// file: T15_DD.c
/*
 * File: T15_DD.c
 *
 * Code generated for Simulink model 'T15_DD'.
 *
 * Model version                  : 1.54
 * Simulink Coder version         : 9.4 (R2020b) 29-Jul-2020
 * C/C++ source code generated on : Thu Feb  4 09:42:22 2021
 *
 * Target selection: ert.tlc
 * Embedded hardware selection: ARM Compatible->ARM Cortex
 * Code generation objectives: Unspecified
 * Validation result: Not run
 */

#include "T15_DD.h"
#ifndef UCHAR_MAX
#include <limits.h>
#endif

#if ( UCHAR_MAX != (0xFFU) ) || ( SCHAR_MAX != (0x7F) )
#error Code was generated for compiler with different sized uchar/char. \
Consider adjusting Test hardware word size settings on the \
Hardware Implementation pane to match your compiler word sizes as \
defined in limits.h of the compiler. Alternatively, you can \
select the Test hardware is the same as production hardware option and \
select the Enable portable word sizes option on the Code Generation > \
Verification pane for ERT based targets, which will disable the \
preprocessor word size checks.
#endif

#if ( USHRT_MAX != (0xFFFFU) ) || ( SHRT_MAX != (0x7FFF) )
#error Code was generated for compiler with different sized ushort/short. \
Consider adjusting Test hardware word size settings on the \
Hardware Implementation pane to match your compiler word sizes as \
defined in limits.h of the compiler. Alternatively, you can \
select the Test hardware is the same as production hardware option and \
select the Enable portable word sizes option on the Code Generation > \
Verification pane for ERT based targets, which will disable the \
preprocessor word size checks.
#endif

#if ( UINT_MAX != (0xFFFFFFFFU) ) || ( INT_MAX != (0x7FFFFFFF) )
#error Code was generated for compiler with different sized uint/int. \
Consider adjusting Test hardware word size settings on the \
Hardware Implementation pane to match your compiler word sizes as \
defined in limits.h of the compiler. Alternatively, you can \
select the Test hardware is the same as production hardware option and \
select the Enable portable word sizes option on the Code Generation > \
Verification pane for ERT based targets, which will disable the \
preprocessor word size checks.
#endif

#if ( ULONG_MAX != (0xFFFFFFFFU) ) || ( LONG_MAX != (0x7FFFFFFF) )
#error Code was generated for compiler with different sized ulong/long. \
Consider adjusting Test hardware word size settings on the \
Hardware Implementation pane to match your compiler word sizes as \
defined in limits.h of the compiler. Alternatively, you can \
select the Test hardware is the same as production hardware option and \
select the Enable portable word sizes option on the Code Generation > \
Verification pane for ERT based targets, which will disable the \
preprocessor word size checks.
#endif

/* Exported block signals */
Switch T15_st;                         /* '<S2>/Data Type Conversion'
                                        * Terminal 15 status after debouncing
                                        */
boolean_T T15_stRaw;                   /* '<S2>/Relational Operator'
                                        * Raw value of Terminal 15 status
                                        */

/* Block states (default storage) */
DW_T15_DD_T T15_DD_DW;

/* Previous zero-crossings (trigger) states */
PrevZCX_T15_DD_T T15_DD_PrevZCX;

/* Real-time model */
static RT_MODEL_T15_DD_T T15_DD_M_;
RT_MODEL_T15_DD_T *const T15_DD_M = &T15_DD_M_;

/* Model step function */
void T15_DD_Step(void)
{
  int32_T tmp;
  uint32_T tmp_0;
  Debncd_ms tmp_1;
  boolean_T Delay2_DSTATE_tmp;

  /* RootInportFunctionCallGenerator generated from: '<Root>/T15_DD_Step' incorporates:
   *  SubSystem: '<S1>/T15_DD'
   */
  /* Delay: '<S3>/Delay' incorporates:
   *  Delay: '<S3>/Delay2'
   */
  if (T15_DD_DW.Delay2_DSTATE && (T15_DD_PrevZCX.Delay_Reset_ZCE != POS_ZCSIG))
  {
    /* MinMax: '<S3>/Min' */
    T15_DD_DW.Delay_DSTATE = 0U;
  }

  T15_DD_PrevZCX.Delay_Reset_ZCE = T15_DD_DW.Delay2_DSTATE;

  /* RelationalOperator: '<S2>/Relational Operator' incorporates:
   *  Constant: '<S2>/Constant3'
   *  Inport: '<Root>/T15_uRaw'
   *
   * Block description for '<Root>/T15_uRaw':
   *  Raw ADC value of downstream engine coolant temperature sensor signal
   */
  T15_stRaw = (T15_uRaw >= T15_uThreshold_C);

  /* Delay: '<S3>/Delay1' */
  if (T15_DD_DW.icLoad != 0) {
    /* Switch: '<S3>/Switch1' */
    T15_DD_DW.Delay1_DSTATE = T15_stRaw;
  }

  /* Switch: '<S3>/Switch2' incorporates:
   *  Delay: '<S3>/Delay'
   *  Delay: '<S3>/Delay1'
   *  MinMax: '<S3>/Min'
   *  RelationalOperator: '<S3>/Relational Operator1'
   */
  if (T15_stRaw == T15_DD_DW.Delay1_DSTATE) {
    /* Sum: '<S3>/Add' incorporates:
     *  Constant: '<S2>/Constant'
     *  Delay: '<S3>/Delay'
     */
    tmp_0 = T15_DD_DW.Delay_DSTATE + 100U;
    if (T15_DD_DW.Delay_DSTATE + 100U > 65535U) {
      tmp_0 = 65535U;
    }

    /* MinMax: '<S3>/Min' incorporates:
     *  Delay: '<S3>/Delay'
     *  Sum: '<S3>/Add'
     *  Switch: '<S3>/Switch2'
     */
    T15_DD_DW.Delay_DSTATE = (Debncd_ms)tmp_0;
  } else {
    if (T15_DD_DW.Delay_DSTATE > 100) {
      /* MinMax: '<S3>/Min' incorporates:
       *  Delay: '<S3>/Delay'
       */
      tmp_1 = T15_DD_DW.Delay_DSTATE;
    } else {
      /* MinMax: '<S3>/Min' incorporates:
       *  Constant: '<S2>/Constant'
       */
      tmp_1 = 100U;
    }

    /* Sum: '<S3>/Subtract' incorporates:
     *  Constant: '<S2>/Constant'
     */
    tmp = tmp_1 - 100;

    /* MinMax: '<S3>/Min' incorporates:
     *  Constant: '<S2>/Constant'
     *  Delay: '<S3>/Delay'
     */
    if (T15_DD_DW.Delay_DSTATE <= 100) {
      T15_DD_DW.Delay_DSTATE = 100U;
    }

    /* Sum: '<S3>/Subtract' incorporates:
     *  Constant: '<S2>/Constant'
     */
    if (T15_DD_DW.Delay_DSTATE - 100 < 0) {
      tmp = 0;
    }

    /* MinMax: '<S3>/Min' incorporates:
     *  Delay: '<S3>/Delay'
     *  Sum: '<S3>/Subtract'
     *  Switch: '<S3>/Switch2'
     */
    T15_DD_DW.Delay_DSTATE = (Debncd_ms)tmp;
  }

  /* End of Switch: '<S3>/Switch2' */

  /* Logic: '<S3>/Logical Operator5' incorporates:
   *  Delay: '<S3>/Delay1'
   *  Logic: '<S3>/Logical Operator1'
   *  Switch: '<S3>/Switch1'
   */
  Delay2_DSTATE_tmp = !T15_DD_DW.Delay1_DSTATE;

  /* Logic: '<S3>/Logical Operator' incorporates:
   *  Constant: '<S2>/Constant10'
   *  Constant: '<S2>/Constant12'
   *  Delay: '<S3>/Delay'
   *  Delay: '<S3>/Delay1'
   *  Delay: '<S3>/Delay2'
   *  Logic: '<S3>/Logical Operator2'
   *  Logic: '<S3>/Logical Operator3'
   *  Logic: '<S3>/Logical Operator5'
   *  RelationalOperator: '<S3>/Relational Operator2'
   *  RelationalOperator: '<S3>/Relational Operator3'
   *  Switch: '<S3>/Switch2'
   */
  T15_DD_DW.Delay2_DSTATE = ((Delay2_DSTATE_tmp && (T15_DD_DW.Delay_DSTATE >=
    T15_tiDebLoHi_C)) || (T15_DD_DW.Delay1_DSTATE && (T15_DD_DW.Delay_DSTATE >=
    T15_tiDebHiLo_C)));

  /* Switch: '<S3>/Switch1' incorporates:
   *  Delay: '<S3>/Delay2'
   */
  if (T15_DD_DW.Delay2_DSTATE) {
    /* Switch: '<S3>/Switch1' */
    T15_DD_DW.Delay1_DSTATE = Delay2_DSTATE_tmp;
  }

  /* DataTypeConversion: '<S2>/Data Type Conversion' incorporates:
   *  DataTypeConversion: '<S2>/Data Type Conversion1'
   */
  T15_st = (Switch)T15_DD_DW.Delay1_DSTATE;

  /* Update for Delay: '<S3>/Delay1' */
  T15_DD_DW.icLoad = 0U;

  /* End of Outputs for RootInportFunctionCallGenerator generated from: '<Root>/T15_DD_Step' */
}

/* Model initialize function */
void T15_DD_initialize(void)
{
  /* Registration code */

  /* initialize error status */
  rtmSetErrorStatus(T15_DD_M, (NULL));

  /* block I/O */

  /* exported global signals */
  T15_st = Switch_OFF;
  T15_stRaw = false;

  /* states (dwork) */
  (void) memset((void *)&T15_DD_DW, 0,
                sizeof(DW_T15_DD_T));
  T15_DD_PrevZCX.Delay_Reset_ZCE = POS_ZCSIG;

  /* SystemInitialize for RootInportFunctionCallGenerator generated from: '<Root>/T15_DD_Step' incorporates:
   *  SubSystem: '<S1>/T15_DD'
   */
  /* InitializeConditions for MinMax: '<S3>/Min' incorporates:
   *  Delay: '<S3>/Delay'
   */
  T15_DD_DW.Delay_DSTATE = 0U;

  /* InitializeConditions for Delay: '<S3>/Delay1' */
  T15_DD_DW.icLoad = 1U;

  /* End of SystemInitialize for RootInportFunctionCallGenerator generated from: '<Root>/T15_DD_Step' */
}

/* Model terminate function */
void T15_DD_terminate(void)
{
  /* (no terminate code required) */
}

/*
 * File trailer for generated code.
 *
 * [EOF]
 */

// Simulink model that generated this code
simulink model "T15_DD"  (R2018a)
settings: configuration reference "cs_ert" (kept outside this file)
model workspace (MAT data in the model file):
  T15_DD_DT = 10
values from neighbouring files (symbols this model uses):
  T15_tiDebHiLo_C = 10.0    [T15_DD.sldd]
  T15_tiDebLoHi_C = 10.0    [T15_DD.sldd]
  T15_uThreshold_C = 800.0    [T15_DD.sldd]
libraries: sllib x1

== system T15_DD ==
  T15_DD_Step : Inport  OutputFunctionCall=on
  T15_uRaw : Inport  Description=Raw ADC value of downstream engine coolant temperature sensor signal  Port=2  OutMin=0  OutMax=5000  OutDataTypeStr=Volt_mV  Unit=mv  PortDimensions=[1 1]
  Overview : Subsystem
  T15_st : Outport  Description=Terminal 15 status after debouncing  OutDataTypeStr=Enum:Switch  PortDimensions=[1 1]
  wires:
  T15_DD_Step/1 -> Overview/1(T15_DD_Step)
  T15_uRaw/1 -> Overview/2(T15_uRaw)
  Overview/1(T15_st) -> T15_st/1

== system T15_DD/Overview ==
  T15_DD_Step : Inport
  T15_uRaw : Inport  Port=2
  T15_DD : Subsystem
  T15_st : Outport
  wires:
  T15_uRaw/1 -> T15_DD/1(T15_uRaw)
  T15_DD/1(T15_st) -> T15_st/1
  T15_DD_Step/1 -> T15_DD/Trigger

== system T15_DD/Overview/T15_DD ==
  note: %大于800mv为高%
  T15_uRaw : Inport  Tag=mv
  Trigger : TriggerPort  TriggerType=function-call  VariantControl=Variant  PortDimensions=1
  Constant : Constant  Value=T15_DD_DT  OutDataTypeStr=Inherit: Inherit via back propagation
  Constant10 : Constant  Value=T15_tiDebLoHi_C
  Constant12 : Constant  Value=T15_tiDebHiLo_C
  Constant3 : Constant  Value=T15_uThreshold_C
  Data Type Conversion : DataTypeConversion
  Data Type Conversion1 : DataTypeConversion  OutDataTypeStr=uint8
  Debounce_DT : sllib/Debounce_DT
  Relational Operator : RelationalOperator  OutDataTypeStr=boolean  RndMeth=Nearest  InputSameDT=on
  T15_st : Outport
  wires:
  Constant3/1 -> Relational Operator/2
  Constant12/1 -> Debounce_DT/3
  Relational Operator/1 -> Debounce_DT/1  "T15_stRaw"
  Data Type Conversion/1 -> T15_st/1  "T15_st"
  Data Type Conversion1/1 -> Data Type Conversion/1
  T15_uRaw/1 -> Relational Operator/1
  Constant/1 -> Debounce_DT/4
  Constant10/1 -> Debounce_DT/2
  Debounce_DT/1 -> Data Type Conversion1/1
